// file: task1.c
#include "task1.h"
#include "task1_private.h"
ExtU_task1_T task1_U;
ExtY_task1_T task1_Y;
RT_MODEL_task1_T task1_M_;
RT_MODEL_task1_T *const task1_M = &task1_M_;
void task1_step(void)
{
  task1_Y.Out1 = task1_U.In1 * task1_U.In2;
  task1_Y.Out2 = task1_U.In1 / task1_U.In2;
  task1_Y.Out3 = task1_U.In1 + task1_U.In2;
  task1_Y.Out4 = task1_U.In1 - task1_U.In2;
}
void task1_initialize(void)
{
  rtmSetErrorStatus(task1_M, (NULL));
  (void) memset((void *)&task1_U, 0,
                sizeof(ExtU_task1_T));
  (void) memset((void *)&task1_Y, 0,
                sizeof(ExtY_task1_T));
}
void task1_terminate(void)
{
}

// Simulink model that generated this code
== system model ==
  In1 : Inport
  In2 : Inport
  Out1 : Outport  <- 1: Product#1
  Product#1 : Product  <- 1: In1, 2: In2
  Out2 : Outport  <- 1: Product#2
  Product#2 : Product  Inputs=*/  <- 1: In1, 2: In2
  Out3 : Outport  <- 1: Sum#1
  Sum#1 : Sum  Inputs=2  <- 1: In1, 2: In2
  Out4 : Outport  <- 1: Sum#2
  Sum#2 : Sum  Inputs=+-  <- 1: In1, 2: In2
